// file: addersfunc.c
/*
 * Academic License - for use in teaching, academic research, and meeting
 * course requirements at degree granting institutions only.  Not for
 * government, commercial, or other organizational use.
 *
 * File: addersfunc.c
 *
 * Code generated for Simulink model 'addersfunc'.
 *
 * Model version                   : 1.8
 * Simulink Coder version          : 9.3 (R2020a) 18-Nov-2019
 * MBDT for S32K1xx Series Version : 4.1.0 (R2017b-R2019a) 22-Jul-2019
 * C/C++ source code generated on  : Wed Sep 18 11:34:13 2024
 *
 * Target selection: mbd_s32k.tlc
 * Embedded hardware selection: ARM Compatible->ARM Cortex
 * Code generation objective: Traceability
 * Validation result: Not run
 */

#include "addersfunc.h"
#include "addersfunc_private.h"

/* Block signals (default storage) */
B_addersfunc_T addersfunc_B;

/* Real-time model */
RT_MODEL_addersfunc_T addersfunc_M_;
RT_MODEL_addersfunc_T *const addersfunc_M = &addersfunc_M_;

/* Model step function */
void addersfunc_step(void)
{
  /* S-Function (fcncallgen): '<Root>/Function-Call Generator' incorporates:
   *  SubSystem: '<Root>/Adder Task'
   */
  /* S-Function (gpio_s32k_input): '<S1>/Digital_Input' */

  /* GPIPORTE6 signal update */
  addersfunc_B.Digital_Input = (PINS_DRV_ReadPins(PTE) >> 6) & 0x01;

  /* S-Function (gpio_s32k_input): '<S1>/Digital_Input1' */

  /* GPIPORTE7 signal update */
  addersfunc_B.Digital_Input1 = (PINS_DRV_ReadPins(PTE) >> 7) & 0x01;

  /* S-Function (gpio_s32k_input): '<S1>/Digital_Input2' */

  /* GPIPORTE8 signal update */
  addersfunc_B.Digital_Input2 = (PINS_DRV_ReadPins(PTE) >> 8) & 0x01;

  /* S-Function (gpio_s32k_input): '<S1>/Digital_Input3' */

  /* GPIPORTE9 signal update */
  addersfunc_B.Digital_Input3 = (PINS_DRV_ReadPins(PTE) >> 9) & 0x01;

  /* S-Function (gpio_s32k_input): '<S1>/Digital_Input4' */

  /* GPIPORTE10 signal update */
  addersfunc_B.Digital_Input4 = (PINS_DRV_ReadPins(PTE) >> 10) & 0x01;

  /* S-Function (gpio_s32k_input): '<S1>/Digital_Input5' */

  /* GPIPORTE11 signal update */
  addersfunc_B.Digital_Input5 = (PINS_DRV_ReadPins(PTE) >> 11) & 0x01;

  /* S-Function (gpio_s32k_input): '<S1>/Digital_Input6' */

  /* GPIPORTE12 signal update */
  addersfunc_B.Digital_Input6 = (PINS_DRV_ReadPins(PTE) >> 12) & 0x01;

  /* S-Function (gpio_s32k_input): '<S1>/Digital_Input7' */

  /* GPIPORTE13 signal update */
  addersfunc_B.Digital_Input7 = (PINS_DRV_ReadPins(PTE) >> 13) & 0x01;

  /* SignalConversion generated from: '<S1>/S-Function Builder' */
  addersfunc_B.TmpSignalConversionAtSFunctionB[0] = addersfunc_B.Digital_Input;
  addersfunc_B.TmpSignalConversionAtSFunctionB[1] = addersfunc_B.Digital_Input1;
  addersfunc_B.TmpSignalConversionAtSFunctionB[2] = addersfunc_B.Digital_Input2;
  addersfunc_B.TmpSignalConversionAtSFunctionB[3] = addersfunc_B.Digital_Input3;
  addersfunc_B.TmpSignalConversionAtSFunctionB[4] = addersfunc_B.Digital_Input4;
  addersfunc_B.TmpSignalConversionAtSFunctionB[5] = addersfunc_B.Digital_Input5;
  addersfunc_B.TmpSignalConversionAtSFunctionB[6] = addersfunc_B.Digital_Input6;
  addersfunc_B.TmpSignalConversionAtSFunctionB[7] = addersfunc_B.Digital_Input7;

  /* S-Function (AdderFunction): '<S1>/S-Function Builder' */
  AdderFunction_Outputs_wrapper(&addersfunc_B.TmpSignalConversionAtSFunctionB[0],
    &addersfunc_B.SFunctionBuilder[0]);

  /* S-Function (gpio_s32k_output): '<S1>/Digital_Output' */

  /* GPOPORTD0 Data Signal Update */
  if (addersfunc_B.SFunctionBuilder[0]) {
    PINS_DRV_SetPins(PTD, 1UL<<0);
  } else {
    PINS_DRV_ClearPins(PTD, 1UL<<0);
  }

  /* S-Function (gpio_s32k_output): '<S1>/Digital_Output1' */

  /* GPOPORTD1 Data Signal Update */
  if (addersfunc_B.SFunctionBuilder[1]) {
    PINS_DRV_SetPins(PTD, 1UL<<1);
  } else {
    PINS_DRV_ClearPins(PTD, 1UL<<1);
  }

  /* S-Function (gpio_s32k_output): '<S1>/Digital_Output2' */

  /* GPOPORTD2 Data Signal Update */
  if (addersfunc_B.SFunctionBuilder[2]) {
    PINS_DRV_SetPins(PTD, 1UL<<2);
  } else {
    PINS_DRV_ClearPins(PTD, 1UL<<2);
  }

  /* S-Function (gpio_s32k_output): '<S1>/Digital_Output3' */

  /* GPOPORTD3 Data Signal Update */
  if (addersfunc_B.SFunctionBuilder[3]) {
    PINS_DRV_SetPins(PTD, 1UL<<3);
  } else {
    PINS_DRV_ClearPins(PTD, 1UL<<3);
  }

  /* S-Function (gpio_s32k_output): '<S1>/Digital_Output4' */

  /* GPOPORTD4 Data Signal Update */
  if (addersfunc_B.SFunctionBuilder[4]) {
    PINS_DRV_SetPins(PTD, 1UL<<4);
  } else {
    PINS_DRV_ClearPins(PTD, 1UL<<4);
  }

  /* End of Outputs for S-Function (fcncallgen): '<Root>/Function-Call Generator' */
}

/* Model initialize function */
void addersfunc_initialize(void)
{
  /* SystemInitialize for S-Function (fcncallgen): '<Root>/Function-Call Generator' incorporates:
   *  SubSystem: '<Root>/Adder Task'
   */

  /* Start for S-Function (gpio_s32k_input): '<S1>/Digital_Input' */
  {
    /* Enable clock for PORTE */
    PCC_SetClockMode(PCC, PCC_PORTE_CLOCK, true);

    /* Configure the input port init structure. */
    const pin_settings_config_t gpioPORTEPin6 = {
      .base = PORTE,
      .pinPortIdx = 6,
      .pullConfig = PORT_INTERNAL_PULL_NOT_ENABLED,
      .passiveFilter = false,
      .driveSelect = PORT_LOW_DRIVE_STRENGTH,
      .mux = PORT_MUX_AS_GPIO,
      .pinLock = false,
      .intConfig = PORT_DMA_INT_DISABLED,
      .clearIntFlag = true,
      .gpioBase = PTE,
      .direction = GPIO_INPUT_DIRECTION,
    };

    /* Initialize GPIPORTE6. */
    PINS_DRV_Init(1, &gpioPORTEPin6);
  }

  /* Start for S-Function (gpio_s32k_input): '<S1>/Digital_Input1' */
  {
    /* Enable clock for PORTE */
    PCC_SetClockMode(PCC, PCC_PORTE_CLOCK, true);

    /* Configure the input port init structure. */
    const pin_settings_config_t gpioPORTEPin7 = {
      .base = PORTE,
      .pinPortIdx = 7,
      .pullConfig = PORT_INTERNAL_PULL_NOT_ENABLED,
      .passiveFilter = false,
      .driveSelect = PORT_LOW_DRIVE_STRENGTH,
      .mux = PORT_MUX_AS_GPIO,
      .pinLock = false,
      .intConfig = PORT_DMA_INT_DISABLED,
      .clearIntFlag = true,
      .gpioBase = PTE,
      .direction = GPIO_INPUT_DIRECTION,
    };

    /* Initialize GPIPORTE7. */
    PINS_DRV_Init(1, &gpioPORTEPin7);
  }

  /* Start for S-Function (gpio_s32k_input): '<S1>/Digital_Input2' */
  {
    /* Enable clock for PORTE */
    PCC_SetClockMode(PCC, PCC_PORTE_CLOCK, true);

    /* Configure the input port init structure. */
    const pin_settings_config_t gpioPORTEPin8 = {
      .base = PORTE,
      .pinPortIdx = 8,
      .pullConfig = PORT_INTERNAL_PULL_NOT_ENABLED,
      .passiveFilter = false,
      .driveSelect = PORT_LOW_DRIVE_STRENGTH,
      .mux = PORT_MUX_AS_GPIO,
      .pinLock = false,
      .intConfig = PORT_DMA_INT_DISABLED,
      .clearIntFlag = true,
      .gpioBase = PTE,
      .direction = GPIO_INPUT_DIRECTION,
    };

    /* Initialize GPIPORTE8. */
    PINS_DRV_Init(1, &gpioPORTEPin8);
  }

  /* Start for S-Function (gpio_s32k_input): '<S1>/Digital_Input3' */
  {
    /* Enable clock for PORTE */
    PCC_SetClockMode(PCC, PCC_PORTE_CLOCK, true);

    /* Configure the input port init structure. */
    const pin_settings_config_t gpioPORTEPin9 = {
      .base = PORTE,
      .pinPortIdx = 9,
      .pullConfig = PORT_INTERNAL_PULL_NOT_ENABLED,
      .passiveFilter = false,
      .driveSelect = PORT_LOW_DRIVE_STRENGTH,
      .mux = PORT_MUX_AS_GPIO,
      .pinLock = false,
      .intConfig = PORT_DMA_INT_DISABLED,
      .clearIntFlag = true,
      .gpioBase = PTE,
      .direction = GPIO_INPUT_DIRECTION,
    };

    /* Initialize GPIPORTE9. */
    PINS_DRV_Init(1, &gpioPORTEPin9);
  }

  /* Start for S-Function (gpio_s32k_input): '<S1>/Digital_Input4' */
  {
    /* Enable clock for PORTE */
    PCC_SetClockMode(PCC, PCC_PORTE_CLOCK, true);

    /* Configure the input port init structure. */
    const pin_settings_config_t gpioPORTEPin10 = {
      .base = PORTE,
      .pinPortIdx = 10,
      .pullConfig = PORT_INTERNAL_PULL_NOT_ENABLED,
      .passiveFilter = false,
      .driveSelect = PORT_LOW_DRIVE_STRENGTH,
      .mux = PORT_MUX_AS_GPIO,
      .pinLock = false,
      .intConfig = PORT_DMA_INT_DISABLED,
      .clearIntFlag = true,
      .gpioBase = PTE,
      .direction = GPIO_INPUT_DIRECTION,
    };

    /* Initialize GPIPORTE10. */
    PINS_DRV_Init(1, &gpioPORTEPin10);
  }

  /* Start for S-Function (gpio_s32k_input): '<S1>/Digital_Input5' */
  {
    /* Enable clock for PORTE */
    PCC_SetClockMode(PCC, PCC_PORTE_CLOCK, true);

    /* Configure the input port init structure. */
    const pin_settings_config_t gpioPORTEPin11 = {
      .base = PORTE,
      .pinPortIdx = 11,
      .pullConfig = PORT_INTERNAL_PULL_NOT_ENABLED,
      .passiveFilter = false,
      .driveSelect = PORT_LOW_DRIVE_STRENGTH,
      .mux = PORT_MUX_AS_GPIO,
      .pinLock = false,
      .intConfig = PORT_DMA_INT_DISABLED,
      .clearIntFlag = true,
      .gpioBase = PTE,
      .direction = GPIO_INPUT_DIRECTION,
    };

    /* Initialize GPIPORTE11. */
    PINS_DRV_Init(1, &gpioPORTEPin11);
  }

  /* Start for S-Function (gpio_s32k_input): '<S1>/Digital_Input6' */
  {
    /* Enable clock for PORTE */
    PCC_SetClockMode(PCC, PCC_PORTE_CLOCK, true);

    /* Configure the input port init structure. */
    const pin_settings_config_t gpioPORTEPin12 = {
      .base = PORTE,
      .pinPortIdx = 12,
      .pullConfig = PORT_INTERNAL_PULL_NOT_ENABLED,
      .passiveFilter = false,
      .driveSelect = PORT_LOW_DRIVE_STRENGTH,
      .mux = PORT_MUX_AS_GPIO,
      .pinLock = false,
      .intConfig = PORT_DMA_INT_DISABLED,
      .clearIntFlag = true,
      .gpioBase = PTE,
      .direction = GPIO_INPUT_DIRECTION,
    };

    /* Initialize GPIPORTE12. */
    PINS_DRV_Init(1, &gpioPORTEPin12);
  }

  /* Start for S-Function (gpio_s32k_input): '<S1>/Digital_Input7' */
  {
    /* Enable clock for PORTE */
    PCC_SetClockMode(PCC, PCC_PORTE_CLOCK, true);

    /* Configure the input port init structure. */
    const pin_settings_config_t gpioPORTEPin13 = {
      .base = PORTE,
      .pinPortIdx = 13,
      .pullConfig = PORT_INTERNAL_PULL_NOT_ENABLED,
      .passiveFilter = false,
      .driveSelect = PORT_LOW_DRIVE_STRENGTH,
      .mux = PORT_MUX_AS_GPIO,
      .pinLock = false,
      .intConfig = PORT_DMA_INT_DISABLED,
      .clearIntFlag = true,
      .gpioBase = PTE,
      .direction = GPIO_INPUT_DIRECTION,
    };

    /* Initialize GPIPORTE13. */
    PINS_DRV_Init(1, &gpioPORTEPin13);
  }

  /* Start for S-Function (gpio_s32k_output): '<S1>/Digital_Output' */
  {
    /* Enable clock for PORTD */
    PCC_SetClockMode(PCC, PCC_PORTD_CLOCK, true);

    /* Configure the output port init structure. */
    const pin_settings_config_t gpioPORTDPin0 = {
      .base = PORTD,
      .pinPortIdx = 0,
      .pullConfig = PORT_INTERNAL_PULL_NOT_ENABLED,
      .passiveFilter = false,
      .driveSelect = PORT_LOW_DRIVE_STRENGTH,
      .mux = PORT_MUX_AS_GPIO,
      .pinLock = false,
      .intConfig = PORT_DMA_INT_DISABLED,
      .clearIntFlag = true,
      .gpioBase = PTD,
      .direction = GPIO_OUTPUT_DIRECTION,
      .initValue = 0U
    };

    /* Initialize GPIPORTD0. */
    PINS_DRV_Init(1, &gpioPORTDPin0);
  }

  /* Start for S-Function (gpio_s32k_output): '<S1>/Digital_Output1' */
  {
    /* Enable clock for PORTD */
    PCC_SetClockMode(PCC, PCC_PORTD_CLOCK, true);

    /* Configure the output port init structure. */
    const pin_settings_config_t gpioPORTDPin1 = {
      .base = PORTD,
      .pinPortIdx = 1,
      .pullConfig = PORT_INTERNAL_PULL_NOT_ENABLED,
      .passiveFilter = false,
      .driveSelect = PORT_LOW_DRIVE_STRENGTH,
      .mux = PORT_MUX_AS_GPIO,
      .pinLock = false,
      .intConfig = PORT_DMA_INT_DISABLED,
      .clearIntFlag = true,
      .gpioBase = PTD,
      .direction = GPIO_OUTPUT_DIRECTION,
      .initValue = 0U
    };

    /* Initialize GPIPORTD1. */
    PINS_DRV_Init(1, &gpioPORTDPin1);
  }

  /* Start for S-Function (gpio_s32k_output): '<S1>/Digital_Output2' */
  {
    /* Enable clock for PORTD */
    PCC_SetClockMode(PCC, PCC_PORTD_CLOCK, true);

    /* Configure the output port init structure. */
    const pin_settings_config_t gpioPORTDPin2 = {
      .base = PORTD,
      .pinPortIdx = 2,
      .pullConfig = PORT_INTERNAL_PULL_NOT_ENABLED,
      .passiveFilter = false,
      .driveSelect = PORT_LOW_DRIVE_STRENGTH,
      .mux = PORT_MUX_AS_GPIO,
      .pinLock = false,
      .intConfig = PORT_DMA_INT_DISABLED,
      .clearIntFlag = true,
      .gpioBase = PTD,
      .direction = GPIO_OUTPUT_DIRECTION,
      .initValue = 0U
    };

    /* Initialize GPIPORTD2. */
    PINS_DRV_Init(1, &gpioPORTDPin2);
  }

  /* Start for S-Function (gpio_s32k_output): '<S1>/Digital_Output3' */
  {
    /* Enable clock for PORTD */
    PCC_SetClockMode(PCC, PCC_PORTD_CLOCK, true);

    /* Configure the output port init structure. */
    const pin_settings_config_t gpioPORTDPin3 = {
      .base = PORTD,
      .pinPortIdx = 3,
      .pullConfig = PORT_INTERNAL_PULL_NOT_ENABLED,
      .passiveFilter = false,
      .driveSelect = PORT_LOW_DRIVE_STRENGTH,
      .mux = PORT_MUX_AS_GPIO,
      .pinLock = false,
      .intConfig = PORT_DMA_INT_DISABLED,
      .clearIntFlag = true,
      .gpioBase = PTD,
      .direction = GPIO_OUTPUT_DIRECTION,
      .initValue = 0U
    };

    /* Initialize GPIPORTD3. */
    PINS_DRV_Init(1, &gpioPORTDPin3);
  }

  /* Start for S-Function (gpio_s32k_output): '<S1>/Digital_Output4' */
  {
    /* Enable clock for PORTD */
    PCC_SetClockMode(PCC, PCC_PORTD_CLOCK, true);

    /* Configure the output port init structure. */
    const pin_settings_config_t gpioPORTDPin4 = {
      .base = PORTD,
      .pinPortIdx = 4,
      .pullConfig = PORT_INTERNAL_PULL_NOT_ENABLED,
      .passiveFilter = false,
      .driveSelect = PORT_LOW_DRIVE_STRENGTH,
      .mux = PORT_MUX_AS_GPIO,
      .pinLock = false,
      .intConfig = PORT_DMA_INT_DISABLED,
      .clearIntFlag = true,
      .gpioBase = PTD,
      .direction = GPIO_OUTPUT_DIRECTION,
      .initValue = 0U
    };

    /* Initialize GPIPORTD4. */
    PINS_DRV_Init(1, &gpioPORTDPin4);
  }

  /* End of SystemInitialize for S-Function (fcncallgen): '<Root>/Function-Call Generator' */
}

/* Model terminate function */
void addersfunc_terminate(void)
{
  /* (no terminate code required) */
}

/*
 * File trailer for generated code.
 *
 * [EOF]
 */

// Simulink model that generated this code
simulink model "addersfunc"  (R2020a)
settings: Solver=FixedStepDiscrete  StartTime=0.0  StopTime=10.0  RelTol=1e-3
InitFcn:
  | mbd_s32k_consistency_checks(bdroot(gcs));
undefined symbols (not defined in the file or in its folder): LQFP
libraries: mbd_s32k1xx_ec_toolbox x14, simulink x1

== system addersfunc ==
  Adder Task : Subsystem
  Function-Call Generator : simulink/Ports & Subsystems/Function-Call Generator  sample_time=0.1  numberOfIterations=1
  MBD_S32K1xx_Config_Information : mbd_s32k1xx_ec_toolbox/MBD_S32K1xx_Config_Information  mbdt_ver=0  disp_str=|  config_params=[]  mcu_target_name=S32K144  mcu_target_package=100-LQFP  mcu_target_sram_size=48KB  mcu_system_clock_freq=80  mcu_xtal_freq=External 8  mcu_steptick_timer=LPIT Channel 0  mcu_steptick_prio=15  ds_import_enable=on  target_compiler=GCC  target_memory=FLASH  gcc_target_compile_opts=-mthumb -mfloat-abi=hard -mfpu=fpv4-sp-d16 -O1 -g -gstrict-dwarf  gcc_target_assemble_opts=-mthumb -mfloat-abi=hard -mfpu=fpv4-sp-d16 -g  gcc_target_link_opts=-mthumb -mfloat-abi=hard -mfpu=fpv4-sp-d16  gcc_target_default_lcf=on  gcc_target_user_lcf=S32K148_192_flash.ld  ghs_target_compile_opts=-cpu=cortexm4f -thumb -fpu=vfpv4_d16 -fsingle -Ogeneral -Wundef -Wimplicit-int -Wshadow -Wtrigraphs --no_commons --gnu_asm -gnu99 -gdwarf-2 -G  ghs_target_assemble_opts=-cpu=cortexm4f -fpu=vfpv4_d16  ghs_target_link_opts=-cpu=cortexm4f -thumb -fpu=vfpv4_d16  ghs_target_default_lcf=on  ghs_target_user_lcf=S32K148_192_flash.ld  iar_target_compile_opts=--cpu=Cortex-M4F --thumb --fpu=VFPv4_sp -Ol -e --debug --dlib_config normal  iar_target_assemble_opts=--cpu Cortex-M4F --thumb --fpu VFPv4_sp  iar_target_link_opts=--no_exceptions --vfe --inline  iar_target_default_lcf=on  iar_target_user_lcf=S32K148_192_flash.icf  pil_download_enable=off  rbl_download_enable=on  rbl_start_delay=5000  rbl_download_interface=OpenSDA  rbl_restart_request=off  rbl_com_port=Custom  rbl_com_port_custom=COM1  pil_download_rate=57600  pil_opensda_drive=F: EVB-S32K144  pil_opensda_drive_custom=D  pil_uart_instance=1  pil_uart_rx=PTC6: [LPUART1_RX | Receive]  pil_uart_tx=PTC7: [LPUART1_TX | Transmit]  FTM_PWM_PcrCheckEnDis=on  FTM_Input_Edge_Inputs_PcrCheckEnDis=on  FTM_Dual_Edge_Inputs_PcrCheckEnDis=on  FTM_Quadrature_Inputs_PcrCheckEnDis=on  FTM_Hall_Sensor_Inputs_PcrCheckEnDis=on  LPTMR_PcrCheckEnDis=on  PIT_PcrCheckEnDis=on  RTC_PcrCheckEnDis=on  FlexCAN_PcrCheckEnDis=on  LIN_PcrCheckEnDis=on  FlexIO_PcrCheckEnDis=on  LPI2C_PcrCheckEnDis=on  LPSPI_PcrCheckEnDis=on  LPUART_PcrCheckEnDis=on  CMP_PcrCheckEnDis=on  GPIO_OutputPcrCheckEnDis=on  GPIO_InputPcrCheckEnDis=on  SBC_PcrCheckEnDis=on  AMMCLIB_PcrCheckEnDis=on  FM_PcrCheckEnDis=on  Profile_PcrCheckEnDis=on  ConfigParams_PcrCheckEnDis=on  ModelRef_PcrCheckEnDis=on  PDB0_PcrCheckEnDis=on  CSEc_PcrCheckEnDis=on  eDMA_PcrCheckEnDis=on  ADC_PcrCheckEnDis=on  WDOG_PcrCheckEnDis=on
      | Target : S32K144-64KB_SRAM
      | Package : 100-pin
      | System clock : 80 MHz
      | XTAL clock : External 8 MHz
      | Compiler : IAR
      | Target Type : FLASH
      | Download Code after build : off
      | Step Tick Interrupt Priority : 15
  wires:
  Function-Call Generator/1 -> Adder Task/Trigger

== system addersfunc/Adder Task ==
  note: Read Lower 4 DIPS
  note: Read Upper 4 DIPS
  note: Write To LEDs
  Trigger : TriggerPort  TriggerType=function-call  VariantControl=Variant  PortDimensions=1
  Demux : Demux  Outputs=5
  Digital_Input : mbd_s32k1xx_ec_toolbox/GPIO Blocks/Digital_Input  gpio_pin=PTE6: [PTE6 | Port E I/O]  pull_resistor=None  passive_filter=off
  Digital_Input1 : mbd_s32k1xx_ec_toolbox/GPIO Blocks/Digital_Input  gpio_pin=PTE7: [PTE7 | Port E I/O]  pull_resistor=None  passive_filter=off
  Digital_Input2 : mbd_s32k1xx_ec_toolbox/GPIO Blocks/Digital_Input  gpio_pin=PTE8: [PTE8 | Port E I/O]  pull_resistor=None  passive_filter=off
  Digital_Input3 : mbd_s32k1xx_ec_toolbox/GPIO Blocks/Digital_Input  gpio_pin=PTE9: [PTE9 | Port E I/O]  pull_resistor=None  passive_filter=off
  Digital_Input4 : mbd_s32k1xx_ec_toolbox/GPIO Blocks/Digital_Input  gpio_pin=PTE10: [PTE10 | Port E I/O]  pull_resistor=None  passive_filter=off
  Digital_Input5 : mbd_s32k1xx_ec_toolbox/GPIO Blocks/Digital_Input  gpio_pin=PTE11: [PTE11 | Port E I/O]  pull_resistor=None  passive_filter=off
  Digital_Input6 : mbd_s32k1xx_ec_toolbox/GPIO Blocks/Digital_Input  gpio_pin=PTE12: [PTE12 | Port E I/O]  pull_resistor=None  passive_filter=off
  Digital_Input7 : mbd_s32k1xx_ec_toolbox/GPIO Blocks/Digital_Input  gpio_pin=PTE13: [PTE13 | Port E I/O]  pull_resistor=None  passive_filter=off
  Digital_Output : mbd_s32k1xx_ec_toolbox/GPIO Blocks/Digital_Output  gpio_pin=PTD0: [PTD0 | Port D I/O]  init_val=Low  drive_strength=Low
  Digital_Output1 : mbd_s32k1xx_ec_toolbox/GPIO Blocks/Digital_Output  gpio_pin=PTD1: [PTD1 | Port D I/O]  init_val=Low  drive_strength=Low
  Digital_Output2 : mbd_s32k1xx_ec_toolbox/GPIO Blocks/Digital_Output  gpio_pin=PTD2: [PTD2 | Port D I/O]  init_val=Low  drive_strength=Low
  Digital_Output3 : mbd_s32k1xx_ec_toolbox/GPIO Blocks/Digital_Output  gpio_pin=PTD3: [PTD3 | Port D I/O]  init_val=Low  drive_strength=Low
  Digital_Output4 : mbd_s32k1xx_ec_toolbox/GPIO Blocks/Digital_Output  gpio_pin=PTD4: [PTD4 | Port D I/O]  init_val=Low  drive_strength=Low
  Mux : Mux  Inputs=8
  S-Function Builder : S-Function  InitFcn=try, set_param(gcb,'FunctionName','AdderFunction'), end  FunctionName=AdderFunction  SFunctionModules=AdderFunction_wrapper  SFunctionDeploymentMode=off  EnableBusSupport=off  mask(S-Function Builder){}
      mask help: Simulink:masks:SFunctionBuilder_MD
      mask init:
      | val = [[.9  0.75 0.75 1 1 .9 .9 1]',[1 1 0.75 0.75 .9 .9 1 .9]'];try , sys = get_param(gcb,'SfunBuilderFcnName');if isempty(sys), sys = get_param(gcb,'FunctionName'); end,catch, sys = get_param(gcb,'FunctionName'); end
  wires:
  Digital_Input3/1 -> Mux/4
  Digital_Input2/1 -> Mux/3
  Digital_Input/1 -> Mux/1
  Digital_Input1/1 -> Mux/2
  Digital_Input4/1 -> Mux/5
  Digital_Input5/1 -> Mux/6
  Digital_Input6/1 -> Mux/7
  Digital_Input7/1 -> Mux/8
  Mux/1 -> S-Function Builder/1
  S-Function Builder/1 -> Demux/1
  Demux/1 -> Digital_Output/1
  Demux/2 -> Digital_Output1/1
  Demux/3 -> Digital_Output2/1
  Demux/4 -> Digital_Output3/1
  Demux/5 -> Digital_Output4/1
